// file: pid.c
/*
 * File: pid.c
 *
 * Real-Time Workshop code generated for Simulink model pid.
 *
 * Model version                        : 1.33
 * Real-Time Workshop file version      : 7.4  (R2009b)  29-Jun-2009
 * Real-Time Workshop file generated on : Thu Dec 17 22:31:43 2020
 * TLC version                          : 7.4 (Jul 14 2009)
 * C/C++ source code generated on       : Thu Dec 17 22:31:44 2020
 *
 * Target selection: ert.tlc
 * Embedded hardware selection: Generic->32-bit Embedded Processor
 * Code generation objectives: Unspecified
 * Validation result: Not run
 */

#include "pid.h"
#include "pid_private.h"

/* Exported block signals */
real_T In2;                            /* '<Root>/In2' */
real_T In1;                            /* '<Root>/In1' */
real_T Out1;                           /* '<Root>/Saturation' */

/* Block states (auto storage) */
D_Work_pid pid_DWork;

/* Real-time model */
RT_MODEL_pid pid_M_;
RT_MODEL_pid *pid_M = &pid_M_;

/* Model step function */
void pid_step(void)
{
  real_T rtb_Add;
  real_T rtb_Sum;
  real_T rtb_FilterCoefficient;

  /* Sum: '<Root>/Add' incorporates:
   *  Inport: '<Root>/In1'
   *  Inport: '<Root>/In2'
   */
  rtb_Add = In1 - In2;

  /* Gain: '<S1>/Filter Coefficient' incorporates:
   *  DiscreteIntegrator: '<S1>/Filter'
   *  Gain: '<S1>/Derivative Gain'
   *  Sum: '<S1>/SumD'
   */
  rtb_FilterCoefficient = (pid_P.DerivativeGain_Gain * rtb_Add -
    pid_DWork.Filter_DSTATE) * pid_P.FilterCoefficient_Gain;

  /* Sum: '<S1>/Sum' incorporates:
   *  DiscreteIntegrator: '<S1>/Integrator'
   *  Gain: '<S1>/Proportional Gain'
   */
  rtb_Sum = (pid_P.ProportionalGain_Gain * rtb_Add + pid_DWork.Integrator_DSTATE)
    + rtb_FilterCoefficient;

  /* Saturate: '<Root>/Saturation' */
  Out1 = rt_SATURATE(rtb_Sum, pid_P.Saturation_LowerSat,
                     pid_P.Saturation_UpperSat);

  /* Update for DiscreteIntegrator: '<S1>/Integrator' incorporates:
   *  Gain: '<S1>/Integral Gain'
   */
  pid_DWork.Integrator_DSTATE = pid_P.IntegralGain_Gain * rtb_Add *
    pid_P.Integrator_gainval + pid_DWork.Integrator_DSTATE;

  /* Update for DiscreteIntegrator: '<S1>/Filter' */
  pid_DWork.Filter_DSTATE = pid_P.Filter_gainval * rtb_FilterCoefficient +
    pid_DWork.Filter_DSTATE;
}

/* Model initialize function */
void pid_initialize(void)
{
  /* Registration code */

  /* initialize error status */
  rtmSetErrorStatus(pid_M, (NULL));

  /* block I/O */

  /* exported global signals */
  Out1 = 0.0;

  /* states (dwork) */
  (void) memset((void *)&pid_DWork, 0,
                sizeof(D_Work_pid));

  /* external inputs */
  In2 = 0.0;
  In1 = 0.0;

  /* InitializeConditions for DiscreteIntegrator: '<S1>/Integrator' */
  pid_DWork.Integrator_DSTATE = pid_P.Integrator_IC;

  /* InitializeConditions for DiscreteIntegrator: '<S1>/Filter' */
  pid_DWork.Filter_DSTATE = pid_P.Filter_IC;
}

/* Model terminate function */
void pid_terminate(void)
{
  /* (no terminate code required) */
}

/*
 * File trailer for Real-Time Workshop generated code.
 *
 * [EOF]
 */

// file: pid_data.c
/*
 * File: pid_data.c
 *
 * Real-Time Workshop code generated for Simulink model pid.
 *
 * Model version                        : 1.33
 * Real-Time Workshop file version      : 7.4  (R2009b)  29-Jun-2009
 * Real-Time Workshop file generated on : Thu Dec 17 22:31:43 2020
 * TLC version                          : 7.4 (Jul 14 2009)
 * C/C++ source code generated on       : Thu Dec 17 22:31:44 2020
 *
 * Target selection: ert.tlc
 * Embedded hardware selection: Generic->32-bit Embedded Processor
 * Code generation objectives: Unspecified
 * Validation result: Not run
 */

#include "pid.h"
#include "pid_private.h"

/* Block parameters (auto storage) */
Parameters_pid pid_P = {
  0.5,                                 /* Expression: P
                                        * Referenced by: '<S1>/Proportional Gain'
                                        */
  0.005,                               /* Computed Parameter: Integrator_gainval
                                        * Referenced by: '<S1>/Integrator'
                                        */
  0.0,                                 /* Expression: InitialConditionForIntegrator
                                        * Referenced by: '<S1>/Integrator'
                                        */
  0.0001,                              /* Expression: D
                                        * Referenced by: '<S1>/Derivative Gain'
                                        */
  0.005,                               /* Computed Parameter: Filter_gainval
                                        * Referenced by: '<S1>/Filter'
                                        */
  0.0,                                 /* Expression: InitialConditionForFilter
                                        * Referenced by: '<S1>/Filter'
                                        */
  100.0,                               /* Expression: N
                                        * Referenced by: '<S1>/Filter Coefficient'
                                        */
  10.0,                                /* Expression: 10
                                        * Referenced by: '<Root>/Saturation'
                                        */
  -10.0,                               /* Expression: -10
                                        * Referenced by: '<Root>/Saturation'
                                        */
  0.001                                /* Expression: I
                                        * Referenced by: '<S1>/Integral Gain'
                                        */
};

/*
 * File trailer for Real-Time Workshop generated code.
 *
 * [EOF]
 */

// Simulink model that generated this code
simulink model "pid"  (Simulink 7.4)
settings: Solver=FixedStepDiscrete  StartTime=0.0  StopTime=100  FixedStep=0.005  RelTol=1e-3
libraries: simulink x1

== system pid ==
  In2 : Inport  OutDataType=fixdt(1, 16)  OutScaling=2^0
  In1 : Inport  Port=2  OutDataType=fixdt(1, 16)  OutScaling=2^0
  Add : Sum  Inputs=+-  OutDataType=fixdt(1, 16)  OutScaling=2^-10
  Discrete PID  Controller : simulink/Continuous/PID Controller  DialogController=pidpack.PIDConfig.pidDDGCreate  DialogControllerArgs=DataTag0  SystemSampleTime=-1  Controller=PID  TimeDomain=Discrete-time  SampleTime=-1  IntegratorMethod=Forward Euler  FilterMethod=Forward Euler  Form=Parallel  P=0.5  I=0.001  D=0.0001  N=100  InitialConditionSource=internal  InitialConditionForIntegrator=0  InitialConditionForFilter=0  ExternalReset=none  LimitOutput=off  UpperSaturationLimit=inf  LowerSaturationLimit=-inf  LinearizeAsGain=off  AntiWindupMode=none  Kb=1  TrackingMode=off  Kt=1  PParamMin=[]  PParamMax=[]  IParamMin=[]  IParamMax=[]  DParamMin=[]  DParamMax=[]  NParamMin=[]  NParamMax=[]  KbParamMin=[]  KbParamMax=[]  KtParamMin=[]  KtParamMax=[]  POutMin=[]  POutMax=[]  IOutMin=[]  IOutMax=[]  DOutMin=[]  DOutMax=[]  NOutMin=[]  NOutMax=[]  KbOutMin=[]  KbOutMax=[]  KtOutMin=[]  KtOutMax=[]  IntegratorOutMin=[]  IntegratorOutMax=[]  FilterOutMin=[]  FilterOutMax=[]  SumOutMin=[]  SumOutMax=[]  SumI1OutMin=[]  SumI1OutMax=[]  SumI2OutMin=[]  SumI2OutMax=[]  SumI3OutMin=[]  SumI3OutMax=[]  SumDOutMin=[]  SumDOutMax=[]  SaturationOutMin=[]  SaturationOutMax=[]  IntegratorContinuousStateAttributes=''  IntegratorStateMustResolveToSignalObject=off  IntegratorRTWStateStorageClass=Auto  FilterContinuousStateAttributes=''  FilterStateMustResolveToSignalObject=off  FilterRTWStateStorageClass=Auto
  Saturation : Saturate  UpperLimit=10  LowerLimit=-10  OutDataType=fixdt(1, 16)  OutScaling=2^0
  Out1 : Outport  OutDataType=fixdt(1, 16)  OutScaling=2^0
  wires:
  Discrete PID  Controller/1 -> Saturation/1  "Out1"
  Add/1 -> Discrete PID  Controller/1
  In1/1 -> Add/1  "In1"
  In2/1 -> Add/2  "In2"
  Saturation/1 -> Out1/1  "Out1"
